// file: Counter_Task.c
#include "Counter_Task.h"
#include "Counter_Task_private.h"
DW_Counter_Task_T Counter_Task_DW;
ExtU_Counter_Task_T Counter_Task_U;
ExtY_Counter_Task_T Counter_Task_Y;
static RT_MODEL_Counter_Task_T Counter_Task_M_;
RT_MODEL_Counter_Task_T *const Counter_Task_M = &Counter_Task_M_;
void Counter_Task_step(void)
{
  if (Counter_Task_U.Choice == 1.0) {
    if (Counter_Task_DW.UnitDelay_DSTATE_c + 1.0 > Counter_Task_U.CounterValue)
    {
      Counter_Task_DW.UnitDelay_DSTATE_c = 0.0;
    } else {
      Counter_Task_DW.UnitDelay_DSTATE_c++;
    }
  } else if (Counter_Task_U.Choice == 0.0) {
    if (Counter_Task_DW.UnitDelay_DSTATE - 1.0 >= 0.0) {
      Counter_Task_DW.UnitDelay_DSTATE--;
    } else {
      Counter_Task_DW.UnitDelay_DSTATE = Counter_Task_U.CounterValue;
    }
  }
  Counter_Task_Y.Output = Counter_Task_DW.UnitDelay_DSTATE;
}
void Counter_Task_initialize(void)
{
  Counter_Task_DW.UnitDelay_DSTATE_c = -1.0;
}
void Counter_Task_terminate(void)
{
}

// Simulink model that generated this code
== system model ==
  CounterValue : Inport
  Choice : Inport
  Output : Outport  <- 1: Merge#1
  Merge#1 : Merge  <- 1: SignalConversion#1, 2: SignalConversion#2
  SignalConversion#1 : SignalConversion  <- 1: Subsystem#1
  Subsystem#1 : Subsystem  <- 1: CounterValue, Action: If#1
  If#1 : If  IfExpression=u1 == 1  ElseIfExpressions=u1 == 0  <- 1: Choice
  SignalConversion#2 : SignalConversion  <- 1: Subsystem#2
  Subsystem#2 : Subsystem  <- 1: CounterValue, Action: If#1/2
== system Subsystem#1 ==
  Inport#1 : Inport
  ActionPort#1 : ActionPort
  Outport#1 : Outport  <- 1: Switch#1
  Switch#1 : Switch  Criteria=u2 ~= 0  <- 1: Constant#1, 2: RelationalOperator#1, 3: Sum#1
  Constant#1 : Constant  Value=0
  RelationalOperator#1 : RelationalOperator  Operator=>  <- 1: Sum#1, 2: Inport#1
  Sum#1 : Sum  <- 1: Constant#2, 2: UnitDelay
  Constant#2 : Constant
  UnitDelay : UnitDelay  InitialCondition=-1  <- 1: Switch#1
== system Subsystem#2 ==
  Inport#2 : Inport
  ActionPort#2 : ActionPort
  Outport#2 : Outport  <- 1: Switch#2
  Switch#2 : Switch  <- 1: Sum#2, 2: Sum#2, 3: Inport#2
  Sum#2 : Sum  Inputs=-+  <- 1: Constant#3, 2: UnitDelay#1
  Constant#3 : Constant
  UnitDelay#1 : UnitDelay  <- 1: Switch#2
